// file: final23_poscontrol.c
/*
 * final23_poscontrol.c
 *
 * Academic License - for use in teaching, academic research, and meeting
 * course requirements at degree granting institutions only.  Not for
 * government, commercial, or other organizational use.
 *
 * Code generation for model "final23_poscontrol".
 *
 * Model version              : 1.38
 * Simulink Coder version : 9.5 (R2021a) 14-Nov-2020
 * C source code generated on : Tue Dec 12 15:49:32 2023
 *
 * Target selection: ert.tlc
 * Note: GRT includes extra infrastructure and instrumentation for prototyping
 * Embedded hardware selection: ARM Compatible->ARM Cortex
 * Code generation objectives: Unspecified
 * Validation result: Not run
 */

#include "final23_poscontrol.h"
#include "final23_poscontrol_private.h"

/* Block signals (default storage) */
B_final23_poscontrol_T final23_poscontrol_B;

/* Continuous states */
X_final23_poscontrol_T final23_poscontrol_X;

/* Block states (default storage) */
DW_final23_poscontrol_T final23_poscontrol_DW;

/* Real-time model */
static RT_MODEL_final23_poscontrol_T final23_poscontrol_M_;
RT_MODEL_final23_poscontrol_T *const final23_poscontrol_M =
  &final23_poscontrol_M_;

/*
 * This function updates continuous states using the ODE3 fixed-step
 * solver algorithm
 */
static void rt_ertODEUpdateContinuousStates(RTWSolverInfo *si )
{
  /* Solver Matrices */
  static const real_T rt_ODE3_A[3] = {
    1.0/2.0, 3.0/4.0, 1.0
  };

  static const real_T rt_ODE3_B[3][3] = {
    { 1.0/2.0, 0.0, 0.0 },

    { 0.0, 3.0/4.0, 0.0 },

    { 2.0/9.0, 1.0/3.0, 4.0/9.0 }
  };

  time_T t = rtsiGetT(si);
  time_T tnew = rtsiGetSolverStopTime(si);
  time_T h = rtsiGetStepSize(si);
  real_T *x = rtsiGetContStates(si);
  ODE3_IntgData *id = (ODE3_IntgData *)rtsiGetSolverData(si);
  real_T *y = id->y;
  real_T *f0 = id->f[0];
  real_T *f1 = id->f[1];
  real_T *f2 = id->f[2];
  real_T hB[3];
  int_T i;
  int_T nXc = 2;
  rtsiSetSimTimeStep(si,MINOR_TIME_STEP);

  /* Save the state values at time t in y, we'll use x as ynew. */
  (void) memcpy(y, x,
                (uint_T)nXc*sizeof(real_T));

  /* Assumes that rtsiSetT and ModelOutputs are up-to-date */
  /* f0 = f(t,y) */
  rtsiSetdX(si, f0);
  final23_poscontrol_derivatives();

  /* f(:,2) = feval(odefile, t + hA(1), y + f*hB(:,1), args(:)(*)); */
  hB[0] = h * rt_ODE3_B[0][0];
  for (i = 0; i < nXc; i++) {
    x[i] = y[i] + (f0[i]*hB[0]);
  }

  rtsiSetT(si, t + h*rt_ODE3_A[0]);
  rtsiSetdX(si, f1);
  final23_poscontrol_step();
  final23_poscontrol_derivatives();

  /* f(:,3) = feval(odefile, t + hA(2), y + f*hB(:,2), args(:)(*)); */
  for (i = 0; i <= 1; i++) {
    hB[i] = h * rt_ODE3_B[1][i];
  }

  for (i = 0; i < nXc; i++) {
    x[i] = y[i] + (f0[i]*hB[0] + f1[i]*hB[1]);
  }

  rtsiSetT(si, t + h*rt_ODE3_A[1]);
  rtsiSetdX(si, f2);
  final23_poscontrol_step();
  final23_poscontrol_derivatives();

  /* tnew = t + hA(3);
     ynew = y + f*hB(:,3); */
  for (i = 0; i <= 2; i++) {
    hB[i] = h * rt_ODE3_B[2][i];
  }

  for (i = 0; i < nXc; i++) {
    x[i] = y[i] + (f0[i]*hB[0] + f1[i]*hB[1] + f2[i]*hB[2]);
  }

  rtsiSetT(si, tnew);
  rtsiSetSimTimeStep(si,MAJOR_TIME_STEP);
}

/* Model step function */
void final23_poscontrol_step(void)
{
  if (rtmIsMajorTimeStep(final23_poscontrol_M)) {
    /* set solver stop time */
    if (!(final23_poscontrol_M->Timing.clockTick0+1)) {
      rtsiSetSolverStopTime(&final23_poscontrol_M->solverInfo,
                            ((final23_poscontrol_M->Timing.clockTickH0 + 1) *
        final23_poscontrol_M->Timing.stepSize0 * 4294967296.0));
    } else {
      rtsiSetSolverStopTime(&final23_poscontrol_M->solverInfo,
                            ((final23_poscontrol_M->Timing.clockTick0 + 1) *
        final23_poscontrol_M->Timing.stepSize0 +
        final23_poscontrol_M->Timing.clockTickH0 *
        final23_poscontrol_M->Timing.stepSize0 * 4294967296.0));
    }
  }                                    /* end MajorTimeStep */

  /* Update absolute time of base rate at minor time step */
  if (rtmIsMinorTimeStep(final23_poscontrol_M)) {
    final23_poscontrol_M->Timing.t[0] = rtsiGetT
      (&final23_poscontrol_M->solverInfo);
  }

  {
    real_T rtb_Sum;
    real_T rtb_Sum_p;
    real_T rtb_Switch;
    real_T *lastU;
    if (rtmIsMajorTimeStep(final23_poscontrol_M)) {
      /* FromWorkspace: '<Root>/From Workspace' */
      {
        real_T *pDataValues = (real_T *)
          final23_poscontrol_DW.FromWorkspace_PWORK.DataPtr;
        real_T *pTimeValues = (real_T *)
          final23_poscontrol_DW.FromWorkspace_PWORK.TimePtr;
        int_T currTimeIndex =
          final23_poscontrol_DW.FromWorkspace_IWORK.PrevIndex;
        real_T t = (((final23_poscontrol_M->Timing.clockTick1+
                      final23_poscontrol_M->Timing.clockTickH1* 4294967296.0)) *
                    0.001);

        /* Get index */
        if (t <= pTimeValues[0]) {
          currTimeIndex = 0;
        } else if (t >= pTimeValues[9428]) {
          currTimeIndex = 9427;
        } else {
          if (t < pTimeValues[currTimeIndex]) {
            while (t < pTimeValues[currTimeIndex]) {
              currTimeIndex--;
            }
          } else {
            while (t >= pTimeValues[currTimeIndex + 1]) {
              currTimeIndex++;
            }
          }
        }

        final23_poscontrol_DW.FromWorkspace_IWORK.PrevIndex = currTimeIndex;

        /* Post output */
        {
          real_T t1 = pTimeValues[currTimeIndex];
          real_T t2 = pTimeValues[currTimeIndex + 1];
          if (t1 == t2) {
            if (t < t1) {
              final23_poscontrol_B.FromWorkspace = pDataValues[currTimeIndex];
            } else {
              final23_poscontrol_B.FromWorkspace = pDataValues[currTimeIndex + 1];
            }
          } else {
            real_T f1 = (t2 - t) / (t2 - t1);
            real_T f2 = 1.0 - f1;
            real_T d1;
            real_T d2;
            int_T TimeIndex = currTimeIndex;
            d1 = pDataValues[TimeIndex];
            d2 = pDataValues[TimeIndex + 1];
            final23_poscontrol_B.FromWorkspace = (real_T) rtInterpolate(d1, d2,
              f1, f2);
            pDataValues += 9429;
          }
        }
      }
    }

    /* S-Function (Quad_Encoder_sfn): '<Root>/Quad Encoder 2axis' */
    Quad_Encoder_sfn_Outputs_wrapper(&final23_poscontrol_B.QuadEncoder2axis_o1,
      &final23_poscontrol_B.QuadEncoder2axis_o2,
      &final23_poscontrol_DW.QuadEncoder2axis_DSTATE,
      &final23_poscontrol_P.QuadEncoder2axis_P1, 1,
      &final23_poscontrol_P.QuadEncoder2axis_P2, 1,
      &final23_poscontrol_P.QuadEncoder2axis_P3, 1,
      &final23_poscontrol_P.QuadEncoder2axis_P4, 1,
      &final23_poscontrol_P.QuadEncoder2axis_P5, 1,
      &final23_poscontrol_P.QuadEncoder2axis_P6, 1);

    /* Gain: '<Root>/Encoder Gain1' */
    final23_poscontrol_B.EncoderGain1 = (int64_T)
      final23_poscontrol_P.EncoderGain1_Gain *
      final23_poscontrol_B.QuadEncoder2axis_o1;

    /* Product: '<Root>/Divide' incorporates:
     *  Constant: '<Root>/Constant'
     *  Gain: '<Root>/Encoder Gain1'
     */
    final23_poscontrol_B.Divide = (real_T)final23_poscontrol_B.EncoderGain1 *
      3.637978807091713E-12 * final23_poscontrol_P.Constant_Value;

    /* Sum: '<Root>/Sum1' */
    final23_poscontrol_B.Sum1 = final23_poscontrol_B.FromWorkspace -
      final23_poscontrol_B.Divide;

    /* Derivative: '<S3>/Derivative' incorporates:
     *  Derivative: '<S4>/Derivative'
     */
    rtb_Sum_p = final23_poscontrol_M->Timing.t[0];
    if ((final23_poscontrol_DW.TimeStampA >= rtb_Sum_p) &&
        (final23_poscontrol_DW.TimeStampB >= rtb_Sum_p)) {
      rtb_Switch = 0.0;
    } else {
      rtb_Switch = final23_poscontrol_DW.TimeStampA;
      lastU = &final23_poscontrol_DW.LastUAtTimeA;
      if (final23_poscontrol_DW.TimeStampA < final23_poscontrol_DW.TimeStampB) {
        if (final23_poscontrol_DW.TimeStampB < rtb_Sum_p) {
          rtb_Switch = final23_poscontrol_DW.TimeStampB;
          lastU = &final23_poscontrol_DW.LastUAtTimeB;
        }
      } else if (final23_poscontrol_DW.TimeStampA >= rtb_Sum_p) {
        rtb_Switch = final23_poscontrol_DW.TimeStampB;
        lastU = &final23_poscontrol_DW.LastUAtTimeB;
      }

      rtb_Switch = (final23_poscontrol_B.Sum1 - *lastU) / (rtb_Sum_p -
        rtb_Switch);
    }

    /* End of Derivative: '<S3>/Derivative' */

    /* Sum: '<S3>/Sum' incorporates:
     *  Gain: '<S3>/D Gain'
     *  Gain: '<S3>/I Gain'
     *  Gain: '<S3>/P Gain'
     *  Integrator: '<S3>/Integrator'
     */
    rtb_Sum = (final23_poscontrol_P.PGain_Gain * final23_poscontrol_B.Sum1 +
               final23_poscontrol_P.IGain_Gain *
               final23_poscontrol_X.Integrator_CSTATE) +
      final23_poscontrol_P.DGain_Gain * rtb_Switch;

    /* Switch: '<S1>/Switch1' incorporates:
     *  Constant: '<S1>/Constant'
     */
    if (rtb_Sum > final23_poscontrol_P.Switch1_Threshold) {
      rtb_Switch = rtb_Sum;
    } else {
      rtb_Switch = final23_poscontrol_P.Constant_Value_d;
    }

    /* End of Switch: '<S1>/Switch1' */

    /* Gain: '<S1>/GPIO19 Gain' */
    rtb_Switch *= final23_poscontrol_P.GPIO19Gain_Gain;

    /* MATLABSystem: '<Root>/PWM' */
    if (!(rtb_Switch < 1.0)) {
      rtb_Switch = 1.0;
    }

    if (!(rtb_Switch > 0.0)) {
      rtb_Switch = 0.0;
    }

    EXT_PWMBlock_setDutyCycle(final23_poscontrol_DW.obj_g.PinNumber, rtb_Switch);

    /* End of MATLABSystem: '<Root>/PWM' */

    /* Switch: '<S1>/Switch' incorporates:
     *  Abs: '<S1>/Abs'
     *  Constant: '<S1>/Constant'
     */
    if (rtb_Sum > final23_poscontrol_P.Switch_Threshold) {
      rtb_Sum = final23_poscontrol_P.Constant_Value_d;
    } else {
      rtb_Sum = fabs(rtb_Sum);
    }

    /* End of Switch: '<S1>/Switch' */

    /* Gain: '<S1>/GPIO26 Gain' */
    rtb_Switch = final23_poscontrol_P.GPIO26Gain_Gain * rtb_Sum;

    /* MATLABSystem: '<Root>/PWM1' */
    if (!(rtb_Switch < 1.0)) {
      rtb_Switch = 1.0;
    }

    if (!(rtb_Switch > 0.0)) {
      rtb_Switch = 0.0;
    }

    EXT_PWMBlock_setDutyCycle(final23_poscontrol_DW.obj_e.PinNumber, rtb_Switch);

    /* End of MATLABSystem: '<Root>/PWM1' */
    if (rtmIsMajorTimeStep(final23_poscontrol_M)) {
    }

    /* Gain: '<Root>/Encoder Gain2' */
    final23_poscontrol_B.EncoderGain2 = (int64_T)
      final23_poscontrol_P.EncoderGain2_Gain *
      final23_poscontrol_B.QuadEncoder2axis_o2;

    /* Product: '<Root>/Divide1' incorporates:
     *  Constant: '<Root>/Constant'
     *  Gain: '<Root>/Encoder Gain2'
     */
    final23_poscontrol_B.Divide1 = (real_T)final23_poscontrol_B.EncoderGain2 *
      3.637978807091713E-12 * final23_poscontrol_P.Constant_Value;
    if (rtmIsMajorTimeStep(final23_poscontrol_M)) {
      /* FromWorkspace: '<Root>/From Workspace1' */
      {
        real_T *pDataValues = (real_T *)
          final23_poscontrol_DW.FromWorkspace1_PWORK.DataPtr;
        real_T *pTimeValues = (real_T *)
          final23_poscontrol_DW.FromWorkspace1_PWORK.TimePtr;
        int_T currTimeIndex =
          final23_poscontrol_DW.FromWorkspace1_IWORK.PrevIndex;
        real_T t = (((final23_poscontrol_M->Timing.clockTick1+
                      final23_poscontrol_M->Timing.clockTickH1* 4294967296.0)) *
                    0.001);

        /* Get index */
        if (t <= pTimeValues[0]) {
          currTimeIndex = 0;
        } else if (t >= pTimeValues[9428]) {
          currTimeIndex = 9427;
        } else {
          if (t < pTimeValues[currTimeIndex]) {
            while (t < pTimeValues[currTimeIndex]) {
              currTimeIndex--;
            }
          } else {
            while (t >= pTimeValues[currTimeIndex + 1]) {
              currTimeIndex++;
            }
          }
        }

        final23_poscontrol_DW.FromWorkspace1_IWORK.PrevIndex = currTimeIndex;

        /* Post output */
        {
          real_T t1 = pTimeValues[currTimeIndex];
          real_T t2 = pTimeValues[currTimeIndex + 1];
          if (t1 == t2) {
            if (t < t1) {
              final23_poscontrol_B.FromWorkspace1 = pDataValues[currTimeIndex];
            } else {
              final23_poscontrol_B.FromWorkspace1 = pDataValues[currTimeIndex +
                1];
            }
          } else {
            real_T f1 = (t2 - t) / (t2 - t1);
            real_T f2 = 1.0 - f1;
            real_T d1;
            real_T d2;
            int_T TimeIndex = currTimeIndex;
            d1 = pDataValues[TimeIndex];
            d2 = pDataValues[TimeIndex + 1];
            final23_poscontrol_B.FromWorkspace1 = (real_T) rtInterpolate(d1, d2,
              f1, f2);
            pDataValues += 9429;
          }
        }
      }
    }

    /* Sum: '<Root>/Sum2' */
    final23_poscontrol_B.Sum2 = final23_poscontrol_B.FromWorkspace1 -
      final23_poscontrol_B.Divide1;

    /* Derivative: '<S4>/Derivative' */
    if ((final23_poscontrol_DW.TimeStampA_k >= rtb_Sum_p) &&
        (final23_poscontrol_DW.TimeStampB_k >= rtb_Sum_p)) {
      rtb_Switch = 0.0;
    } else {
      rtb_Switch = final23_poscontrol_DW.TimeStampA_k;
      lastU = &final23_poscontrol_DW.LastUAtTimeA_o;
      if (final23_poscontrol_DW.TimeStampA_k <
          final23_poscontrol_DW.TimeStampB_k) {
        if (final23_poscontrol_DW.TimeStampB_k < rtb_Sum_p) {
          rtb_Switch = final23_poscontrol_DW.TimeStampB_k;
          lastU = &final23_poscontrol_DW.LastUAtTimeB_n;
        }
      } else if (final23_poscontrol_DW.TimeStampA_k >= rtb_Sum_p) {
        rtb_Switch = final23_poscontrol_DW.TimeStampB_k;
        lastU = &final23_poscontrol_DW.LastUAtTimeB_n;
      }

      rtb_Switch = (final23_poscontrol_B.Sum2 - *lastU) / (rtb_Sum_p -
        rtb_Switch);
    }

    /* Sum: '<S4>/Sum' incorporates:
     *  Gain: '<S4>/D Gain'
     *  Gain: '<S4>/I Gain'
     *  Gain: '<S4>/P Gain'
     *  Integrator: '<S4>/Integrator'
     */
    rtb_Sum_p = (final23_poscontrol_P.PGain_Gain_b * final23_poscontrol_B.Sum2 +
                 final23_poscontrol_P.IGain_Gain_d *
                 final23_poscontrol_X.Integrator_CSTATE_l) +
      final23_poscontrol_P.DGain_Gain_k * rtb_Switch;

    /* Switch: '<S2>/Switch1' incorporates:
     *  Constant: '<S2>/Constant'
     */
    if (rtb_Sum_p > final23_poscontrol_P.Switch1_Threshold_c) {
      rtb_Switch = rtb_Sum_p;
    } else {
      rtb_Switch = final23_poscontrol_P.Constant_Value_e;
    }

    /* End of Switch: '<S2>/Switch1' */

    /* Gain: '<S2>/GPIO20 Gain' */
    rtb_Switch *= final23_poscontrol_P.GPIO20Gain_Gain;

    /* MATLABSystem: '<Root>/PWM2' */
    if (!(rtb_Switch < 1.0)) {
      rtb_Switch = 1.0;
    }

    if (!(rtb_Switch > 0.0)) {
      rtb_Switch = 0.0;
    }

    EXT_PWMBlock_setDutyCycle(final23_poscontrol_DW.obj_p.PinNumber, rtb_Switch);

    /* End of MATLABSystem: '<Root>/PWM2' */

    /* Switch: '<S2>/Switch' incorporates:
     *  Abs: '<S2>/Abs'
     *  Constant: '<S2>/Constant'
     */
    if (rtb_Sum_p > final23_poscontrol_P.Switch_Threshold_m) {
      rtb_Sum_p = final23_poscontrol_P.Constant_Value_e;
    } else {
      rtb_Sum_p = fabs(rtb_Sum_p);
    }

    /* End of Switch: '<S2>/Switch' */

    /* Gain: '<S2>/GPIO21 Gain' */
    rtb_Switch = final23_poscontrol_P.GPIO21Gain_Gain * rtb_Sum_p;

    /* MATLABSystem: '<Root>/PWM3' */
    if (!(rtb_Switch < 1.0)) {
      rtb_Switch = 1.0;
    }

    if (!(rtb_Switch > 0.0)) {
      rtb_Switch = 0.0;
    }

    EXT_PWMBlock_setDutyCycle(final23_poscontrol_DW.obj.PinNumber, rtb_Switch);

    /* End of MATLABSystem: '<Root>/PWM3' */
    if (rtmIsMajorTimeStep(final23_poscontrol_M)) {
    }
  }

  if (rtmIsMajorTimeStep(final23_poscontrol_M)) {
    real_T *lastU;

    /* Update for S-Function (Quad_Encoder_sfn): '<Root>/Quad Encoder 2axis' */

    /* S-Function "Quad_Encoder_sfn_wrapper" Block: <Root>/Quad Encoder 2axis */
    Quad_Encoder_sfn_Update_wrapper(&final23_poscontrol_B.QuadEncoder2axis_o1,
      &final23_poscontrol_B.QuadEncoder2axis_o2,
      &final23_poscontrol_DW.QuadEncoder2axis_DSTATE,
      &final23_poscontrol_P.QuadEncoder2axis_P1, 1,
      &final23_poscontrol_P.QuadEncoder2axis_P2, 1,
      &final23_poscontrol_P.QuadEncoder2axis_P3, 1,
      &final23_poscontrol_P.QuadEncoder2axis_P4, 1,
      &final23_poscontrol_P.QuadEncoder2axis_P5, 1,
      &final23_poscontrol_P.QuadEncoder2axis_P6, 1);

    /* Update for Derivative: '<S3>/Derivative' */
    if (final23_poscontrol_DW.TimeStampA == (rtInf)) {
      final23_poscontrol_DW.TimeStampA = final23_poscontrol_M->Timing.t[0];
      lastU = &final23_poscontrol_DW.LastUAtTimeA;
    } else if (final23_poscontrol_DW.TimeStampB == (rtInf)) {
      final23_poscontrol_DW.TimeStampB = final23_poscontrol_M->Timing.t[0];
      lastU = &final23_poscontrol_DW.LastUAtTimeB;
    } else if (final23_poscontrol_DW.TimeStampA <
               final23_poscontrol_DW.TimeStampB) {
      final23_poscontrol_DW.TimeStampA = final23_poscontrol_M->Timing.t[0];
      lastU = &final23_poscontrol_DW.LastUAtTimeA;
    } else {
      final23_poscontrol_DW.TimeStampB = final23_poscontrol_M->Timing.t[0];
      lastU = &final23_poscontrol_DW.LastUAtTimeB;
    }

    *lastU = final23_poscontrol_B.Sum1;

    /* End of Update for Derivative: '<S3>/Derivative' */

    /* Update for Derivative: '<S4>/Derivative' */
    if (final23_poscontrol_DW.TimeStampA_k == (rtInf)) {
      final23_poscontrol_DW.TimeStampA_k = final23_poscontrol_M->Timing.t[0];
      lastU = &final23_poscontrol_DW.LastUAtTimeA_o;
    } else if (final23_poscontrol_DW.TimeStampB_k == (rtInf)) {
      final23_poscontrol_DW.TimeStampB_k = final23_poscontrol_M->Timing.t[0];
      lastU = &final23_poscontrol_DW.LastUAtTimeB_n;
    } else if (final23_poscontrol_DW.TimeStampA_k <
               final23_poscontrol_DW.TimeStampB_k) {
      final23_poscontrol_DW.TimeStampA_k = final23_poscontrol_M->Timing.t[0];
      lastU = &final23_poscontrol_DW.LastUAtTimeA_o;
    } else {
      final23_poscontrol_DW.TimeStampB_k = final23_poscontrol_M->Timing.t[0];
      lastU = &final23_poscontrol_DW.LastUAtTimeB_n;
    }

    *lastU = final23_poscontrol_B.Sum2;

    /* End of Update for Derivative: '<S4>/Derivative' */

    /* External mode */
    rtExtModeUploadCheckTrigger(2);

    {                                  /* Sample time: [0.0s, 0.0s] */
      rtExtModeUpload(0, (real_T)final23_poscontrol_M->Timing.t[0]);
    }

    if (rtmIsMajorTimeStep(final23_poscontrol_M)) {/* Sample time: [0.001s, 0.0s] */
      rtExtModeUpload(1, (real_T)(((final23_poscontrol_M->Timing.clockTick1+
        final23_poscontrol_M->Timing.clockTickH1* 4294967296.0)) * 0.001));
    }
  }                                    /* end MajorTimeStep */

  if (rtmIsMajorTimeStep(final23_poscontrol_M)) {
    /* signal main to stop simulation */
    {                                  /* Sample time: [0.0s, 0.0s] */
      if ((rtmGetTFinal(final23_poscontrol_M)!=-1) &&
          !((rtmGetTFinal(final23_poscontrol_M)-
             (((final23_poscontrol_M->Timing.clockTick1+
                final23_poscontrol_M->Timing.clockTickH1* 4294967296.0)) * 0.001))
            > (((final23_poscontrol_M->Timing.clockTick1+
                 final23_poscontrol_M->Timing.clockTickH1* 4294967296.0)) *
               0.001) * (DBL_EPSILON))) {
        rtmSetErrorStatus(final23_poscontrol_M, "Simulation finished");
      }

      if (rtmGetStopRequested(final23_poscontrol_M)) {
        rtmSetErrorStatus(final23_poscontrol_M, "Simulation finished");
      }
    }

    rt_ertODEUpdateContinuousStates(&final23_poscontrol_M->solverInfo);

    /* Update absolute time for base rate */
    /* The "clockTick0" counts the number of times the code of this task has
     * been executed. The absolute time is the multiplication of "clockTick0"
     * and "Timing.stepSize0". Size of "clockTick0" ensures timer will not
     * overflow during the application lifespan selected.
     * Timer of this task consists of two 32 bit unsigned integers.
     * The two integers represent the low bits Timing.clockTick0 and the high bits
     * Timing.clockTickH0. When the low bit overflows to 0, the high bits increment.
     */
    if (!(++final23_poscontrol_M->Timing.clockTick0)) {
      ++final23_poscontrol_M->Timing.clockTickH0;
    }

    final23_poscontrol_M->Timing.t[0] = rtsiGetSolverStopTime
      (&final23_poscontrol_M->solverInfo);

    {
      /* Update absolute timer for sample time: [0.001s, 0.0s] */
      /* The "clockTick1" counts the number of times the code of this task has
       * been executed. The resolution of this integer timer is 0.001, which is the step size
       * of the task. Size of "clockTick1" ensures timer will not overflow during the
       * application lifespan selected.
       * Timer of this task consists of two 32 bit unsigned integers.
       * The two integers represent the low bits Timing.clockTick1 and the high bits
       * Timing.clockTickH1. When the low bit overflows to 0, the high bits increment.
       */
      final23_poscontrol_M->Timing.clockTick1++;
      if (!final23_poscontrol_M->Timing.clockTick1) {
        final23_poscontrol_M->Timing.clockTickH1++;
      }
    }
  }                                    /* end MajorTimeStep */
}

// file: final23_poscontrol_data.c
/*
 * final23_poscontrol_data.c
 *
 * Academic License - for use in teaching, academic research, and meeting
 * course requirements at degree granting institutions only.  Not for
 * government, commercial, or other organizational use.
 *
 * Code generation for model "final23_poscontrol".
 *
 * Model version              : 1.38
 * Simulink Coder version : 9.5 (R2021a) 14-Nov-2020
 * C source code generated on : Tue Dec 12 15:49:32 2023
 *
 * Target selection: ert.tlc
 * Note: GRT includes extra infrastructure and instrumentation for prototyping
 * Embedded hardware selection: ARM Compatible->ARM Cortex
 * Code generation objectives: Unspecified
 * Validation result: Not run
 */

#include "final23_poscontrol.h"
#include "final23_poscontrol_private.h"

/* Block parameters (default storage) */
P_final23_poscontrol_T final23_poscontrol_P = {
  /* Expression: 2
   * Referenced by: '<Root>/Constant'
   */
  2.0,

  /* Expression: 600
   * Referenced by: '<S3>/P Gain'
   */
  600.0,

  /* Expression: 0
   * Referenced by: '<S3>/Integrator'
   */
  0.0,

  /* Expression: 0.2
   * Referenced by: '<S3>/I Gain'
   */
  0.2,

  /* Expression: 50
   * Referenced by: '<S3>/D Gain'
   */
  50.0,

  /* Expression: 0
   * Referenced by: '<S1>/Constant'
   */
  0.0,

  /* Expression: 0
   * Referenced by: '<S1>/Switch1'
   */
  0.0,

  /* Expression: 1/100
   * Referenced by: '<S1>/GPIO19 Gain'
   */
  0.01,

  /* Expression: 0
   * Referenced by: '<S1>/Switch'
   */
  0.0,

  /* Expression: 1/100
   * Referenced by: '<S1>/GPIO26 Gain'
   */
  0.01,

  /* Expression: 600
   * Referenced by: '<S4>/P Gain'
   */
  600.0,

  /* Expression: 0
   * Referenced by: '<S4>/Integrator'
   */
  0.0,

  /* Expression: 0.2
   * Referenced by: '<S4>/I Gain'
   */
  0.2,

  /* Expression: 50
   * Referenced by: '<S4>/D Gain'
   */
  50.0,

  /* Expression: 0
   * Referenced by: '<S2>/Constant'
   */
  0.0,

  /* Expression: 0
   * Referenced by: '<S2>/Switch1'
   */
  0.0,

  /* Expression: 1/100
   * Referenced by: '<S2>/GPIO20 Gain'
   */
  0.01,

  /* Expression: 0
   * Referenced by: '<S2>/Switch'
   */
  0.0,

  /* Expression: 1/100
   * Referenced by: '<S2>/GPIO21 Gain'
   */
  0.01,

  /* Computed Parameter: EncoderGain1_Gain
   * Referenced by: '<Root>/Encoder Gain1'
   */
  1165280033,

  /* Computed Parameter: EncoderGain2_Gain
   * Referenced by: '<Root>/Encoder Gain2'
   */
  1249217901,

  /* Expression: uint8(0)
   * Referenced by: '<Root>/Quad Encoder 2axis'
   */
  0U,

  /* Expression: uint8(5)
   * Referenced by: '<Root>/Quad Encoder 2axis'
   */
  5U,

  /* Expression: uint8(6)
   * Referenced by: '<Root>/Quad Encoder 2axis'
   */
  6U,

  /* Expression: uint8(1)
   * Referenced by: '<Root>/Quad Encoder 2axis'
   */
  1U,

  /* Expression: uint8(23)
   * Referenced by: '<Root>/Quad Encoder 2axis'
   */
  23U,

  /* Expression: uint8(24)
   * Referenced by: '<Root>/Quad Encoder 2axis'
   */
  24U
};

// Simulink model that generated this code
simulink model "final23_poscontrol"  (R2021a)
settings: Solver=FixedStepAuto  StartTime=0.0  StopTime=inf  FixedStep=0.001  RelTol=1e-3  EnableMultiTasking=on
StopFcn:
  | mypi=raspi();
  | writeDigitalPin(mypi,19,0);
  | writeDigitalPin(mypi,26,0);
  | writeDigitalPin(mypi,20,0);
  | writeDigitalPin(mypi,21,0);
  | clear mypi;
libraries: raspberrypiBasiclib x4

== system final23_poscontrol ==
  Constant : Constant  Value=2
  Divide : Product  Inputs=**
  Divide1 : Product  Inputs=**
  Encoder Gain1 : Gain  Gain=1/235.89
  Encoder Gain2 : Gain  Gain=1/220.04
  From Workspace : FromWorkspace  VariableName=xInput  SampleTime=0.001
  From Workspace1 : FromWorkspace  VariableName=yInput  SampleTime=0.001
  Motor Subsystem : Subsystem
  Motor Subsystem1 : Subsystem
  PID Subsystem : Subsystem
  PID Subsystem1 : Subsystem
  PWM : raspberrypiBasiclib/PWM  board=Pi 4 Model B  Pin_=19  Frequency=1000  blockPlatform=Raspberry Pi
  PWM1 : raspberrypiBasiclib/PWM  board=Pi 4 Model B  Pin_=26  Frequency=1000  blockPlatform=Raspberry Pi
  PWM2 : raspberrypiBasiclib/PWM  board=Pi 4 Model B  Pin_=20  Frequency=1000  blockPlatform=Raspberry Pi
  PWM3 : raspberrypiBasiclib/PWM  board=Pi 4 Model B  Pin_=21  Frequency=1000  blockPlatform=Raspberry Pi
  Quad Encoder 2axis : S-Function  InitFcn=try, set_param(gcb,'FunctionName','Quad_Encoder_sfn'), end  FunctionName=Quad_Encoder_sfn  Parameters=uint8(0),uint8(5),uint8(6),uint8(1),uint8(23),uint8(24)  SFunctionModules=Quad_Encoder_sfn_wrapper  SFunctionDeploymentMode=off  EnableBusSupport=off  mask(S-Function Builder){}
      mask init:
      | val = [[.9  0.75 0.75 1 1 .9 .9 1]',[1 1 0.75 0.75 .9 .9 1 .9]'];try , sys = get_param(gcb,'SfunBuilderFcnName');if isempty(sys), sys = get_param(gcb,'FunctionName'); end,catch, sys = get_param(gcb,'FunctionName'); end
  Sum1 : Sum  Inputs=|+-
  Sum2 : Sum  Inputs=-+|
  To Workspace1 : ToWorkspace  VariableName=xpos  SampleTime=0.001
  To Workspace2 : ToWorkspace  VariableName=ypos  SampleTime=0.001
  wires:
  Quad Encoder 2axis/1 -> Encoder Gain1/1
  Quad Encoder 2axis/2 -> Encoder Gain2/1
  Sum1/1 -> PID Subsystem/1(In1)
  PID Subsystem/1(Out1) -> Motor Subsystem/1(In1)
  Motor Subsystem/1(Out1) -> PWM/1
  Motor Subsystem/2(Out2) -> PWM1/1
  Motor Subsystem1/2(Out2) -> PWM3/1
  Motor Subsystem1/1(Out1) -> PWM2/1
  PID Subsystem1/1(Out1) -> Motor Subsystem1/1(In1)
  Sum2/1 -> PID Subsystem1/1(In1)
  From Workspace/1 -> Sum1/1
  From Workspace1/1 -> Sum2/2
  Encoder Gain1/1 -> Divide/1
  Encoder Gain2/1 -> Divide1/2
  Divide1/1 -> To Workspace2/1, Sum2/1
  Divide/1 -> Sum1/2, To Workspace1/1
  Constant/1 -> Divide1/1, Divide/2

== system final23_poscontrol/Motor Subsystem ==
  In1 : Inport
  Abs : Abs
  Constant : Constant  Value=0
  GPIO19 Gain : Gain  Gain=1/100
  GPIO26 Gain : Gain  Gain=1/100
  Switch : Switch  Criteria=u2 > Threshold
  Switch1 : Switch  Criteria=u2 > Threshold
  Out1 : Outport
  Out2 : Outport  Port=2
  wires:
  Switch/1 -> GPIO26 Gain/1
  Abs/1 -> Switch/3
  Switch1/1 -> GPIO19 Gain/1
  In1/1 -> Abs/1, Switch/2, Switch1/1, Switch1/2
  Constant/1 -> Switch/1, Switch1/3
  GPIO26 Gain/1 -> Out2/1
  GPIO19 Gain/1 -> Out1/1

== system final23_poscontrol/Motor Subsystem1 ==
  In1 : Inport
  Abs : Abs
  Constant : Constant  Value=0
  GPIO20 Gain : Gain  Gain=1/100
  GPIO21 Gain : Gain  Gain=1/100
  Switch : Switch  Criteria=u2 > Threshold
  Switch1 : Switch  Criteria=u2 > Threshold
  Out1 : Outport
  Out2 : Outport  Port=2
  wires:
  Switch/1 -> GPIO21 Gain/1
  Abs/1 -> Switch/3
  Switch1/1 -> GPIO20 Gain/1
  In1/1 -> Abs/1, Switch/2, Switch1/1, Switch1/2
  Constant/1 -> Switch/1, Switch1/3
  GPIO21 Gain/1 -> Out2/1
  GPIO20 Gain/1 -> Out1/1

== system final23_poscontrol/PID Subsystem ==
  In1 : Inport
  D Gain : Gain  Gain=50
  Derivative : Derivative
  I Gain : Gain  Gain=0.2
  Integrator : Integrator
  P Gain : Gain  Gain=600
  Sum : Sum  Inputs=+++
  Out1 : Outport
  wires:
  Derivative/1 -> D Gain/1
  I Gain/1 -> Sum/2
  Integrator/1 -> I Gain/1
  P Gain/1 -> Sum/1
  D Gain/1 -> Sum/3
  Sum/1 -> Out1/1
  In1/1 -> P Gain/1, Derivative/1, Integrator/1

== system final23_poscontrol/PID Subsystem1 ==
  In1 : Inport
  D Gain : Gain  Gain=50
  Derivative : Derivative
  I Gain : Gain  Gain=0.2
  Integrator : Integrator
  P Gain : Gain  Gain=600
  Sum : Sum  Inputs=+++
  Out1 : Outport
  wires:
  Derivative/1 -> D Gain/1
  I Gain/1 -> Sum/2
  Integrator/1 -> I Gain/1
  P Gain/1 -> Sum/1
  D Gain/1 -> Sum/3
  Sum/1 -> Out1/1
  In1/1 -> P Gain/1, Derivative/1, Integrator/1
